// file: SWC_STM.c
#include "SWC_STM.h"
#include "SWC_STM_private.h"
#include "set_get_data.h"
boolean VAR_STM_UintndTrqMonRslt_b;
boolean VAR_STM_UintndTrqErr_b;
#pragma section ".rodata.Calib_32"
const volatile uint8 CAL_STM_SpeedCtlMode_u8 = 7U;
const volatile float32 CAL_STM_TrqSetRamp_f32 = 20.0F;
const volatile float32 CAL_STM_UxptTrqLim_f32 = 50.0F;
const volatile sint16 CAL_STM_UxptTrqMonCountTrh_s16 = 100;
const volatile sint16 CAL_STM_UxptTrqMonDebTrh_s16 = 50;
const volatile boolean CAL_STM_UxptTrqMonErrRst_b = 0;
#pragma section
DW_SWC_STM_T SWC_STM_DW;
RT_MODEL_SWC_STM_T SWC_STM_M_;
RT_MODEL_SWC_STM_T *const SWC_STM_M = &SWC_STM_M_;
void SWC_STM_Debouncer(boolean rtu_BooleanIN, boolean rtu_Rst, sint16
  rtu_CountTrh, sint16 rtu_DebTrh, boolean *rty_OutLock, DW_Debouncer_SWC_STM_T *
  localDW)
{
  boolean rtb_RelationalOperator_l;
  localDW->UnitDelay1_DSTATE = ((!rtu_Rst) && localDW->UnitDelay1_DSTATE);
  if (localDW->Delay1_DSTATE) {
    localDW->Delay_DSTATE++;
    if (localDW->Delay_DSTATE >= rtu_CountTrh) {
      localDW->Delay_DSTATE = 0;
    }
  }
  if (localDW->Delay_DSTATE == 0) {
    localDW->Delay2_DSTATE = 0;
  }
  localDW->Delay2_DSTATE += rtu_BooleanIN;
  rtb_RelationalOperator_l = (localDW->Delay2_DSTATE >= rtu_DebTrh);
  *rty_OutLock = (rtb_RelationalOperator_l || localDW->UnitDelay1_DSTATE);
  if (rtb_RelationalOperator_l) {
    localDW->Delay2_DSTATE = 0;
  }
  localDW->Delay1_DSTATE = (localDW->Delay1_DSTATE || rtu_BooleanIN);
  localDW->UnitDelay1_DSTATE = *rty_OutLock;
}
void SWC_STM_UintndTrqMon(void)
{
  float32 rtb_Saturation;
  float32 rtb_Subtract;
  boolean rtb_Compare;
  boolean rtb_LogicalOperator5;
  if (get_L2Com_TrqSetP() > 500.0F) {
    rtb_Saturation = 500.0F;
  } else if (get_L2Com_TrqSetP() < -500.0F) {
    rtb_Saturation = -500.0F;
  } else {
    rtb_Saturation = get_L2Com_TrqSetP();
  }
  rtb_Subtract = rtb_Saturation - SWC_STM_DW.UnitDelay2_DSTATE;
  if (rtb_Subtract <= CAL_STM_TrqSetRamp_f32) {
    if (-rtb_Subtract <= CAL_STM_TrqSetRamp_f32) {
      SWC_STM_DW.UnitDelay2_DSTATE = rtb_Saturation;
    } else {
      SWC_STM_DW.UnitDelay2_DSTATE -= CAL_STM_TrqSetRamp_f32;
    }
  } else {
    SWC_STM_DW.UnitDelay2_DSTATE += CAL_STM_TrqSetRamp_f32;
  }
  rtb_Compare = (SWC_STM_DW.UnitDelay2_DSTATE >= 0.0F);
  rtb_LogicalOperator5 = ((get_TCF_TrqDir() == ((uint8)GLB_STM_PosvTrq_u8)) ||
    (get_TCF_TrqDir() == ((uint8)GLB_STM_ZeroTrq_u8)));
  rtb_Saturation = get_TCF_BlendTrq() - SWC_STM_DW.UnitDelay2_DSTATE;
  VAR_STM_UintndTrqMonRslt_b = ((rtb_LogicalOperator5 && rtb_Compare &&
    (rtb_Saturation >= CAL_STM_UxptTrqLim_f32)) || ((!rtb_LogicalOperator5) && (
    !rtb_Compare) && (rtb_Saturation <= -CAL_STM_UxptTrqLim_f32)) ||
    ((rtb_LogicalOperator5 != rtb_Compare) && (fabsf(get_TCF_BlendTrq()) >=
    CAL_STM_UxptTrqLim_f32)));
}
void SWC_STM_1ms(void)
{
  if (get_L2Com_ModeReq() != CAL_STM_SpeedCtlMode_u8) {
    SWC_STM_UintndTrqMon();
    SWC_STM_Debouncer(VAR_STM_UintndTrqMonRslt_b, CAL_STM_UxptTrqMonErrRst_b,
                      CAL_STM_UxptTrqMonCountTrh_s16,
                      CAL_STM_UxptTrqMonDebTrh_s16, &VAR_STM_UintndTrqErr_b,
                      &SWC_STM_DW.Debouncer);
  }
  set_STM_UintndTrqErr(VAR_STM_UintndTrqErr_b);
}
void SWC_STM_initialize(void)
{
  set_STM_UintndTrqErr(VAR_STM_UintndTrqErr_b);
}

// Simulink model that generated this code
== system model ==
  SWC_STM_1ms : Inport
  L2Com_ModeReq : Inport
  TCF_BlendTrq : Inport
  L2Com_TrqSetP : Inport
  TCF_TrqDir : Inport
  STM_UintndTrqErr : Outport  <- 1: Subsystem#1
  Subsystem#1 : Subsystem  <- 1: L2Com_ModeReq, 2: TCF_BlendTrq, 3: L2Com_TrqSetP, 4: TCF_TrqDir, Trigger: SWC_STM_1ms
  EventListener#1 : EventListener
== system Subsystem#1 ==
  Inport#1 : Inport
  Inport#2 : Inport
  Inport#3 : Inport
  Inport#4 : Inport
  TriggerPort#1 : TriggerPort  TriggerType=function-call
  Outport#1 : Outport  <- 1: SignalConversion#1
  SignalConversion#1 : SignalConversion  <- 1: Subsystem#2
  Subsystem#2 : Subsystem  <- 1: Inport#2, 2: Inport#3, 3: Inport#4, Enable: Subsystem#3
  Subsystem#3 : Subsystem  <- 1: Inport#1
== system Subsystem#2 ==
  Inport#5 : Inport
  Inport#6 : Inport
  Inport#7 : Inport
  EnablePort#1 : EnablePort
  Outport#2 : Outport  <- 1: Debouncer
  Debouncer : Subsystem  <- 1: UintndTrqMon, 2: Constant#1, 3: Constant#2, 4: Constant#3
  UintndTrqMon : Subsystem  <- 1: Inport#5, 2: Inport#6, 3: Inport#7
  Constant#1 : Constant  Value=CAL_STM_UxptTrqMonErrRst_b
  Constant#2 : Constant  Value=CAL_STM_UxptTrqMonCountTrh_s16
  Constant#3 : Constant  Value=CAL_STM_UxptTrqMonDebTrh_s16
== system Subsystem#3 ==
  Inport#8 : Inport
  Outport#3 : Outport  <- 1: RelationalOperator#1
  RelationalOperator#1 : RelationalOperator  Operator=~=  <- 1: Inport#8, 2: Constant#4
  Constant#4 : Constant  Value=CAL_STM_SpeedCtlMode_u8
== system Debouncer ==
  BooleanIN : Inport
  Rst : Inport
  CountTrh : Inport
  DebTrh : Inport
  OutLock : Outport  <- 1: Logic#1
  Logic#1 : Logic  Operator=OR  <- 1: RelationalOperator, 2: Switch#1
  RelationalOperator : RelationalOperator  <- 1: Sum#1, 2: DebTrh
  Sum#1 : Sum  <- 1: BooleanIN, 2: Switch#2
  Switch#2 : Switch  Criteria=u2 > Threshold  <- 1: Constant#5, 2: CompareToZero#1, 3: Delay2
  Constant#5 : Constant  Value=0
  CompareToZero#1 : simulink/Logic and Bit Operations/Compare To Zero  relop===  <- 1: Subsystem#4
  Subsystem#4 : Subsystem  <- 1: CountTrh, Enable: Delay1
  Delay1 : Delay  DelayLength=1  <- 1: Logic#2
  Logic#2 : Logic  Operator=OR  <- 1: Delay1, 2: BooleanIN
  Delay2 : Delay  DelayLength=1  <- 1: Switch#3
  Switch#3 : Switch  Criteria=u2 > Threshold  <- 1: Constant#6, 2: RelationalOperator, 3: Sum#1
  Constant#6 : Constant  Value=0
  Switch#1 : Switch  Criteria=u2 ~= 0  <- 1: Constant#7, 2: Rst, 3: UnitDelay1
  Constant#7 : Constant  Value=0
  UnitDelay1 : UnitDelay  <- 1: Logic#1
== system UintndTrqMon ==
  Inport#9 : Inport
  Inport#10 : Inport
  Inport#11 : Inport
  Outport#4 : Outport  <- 1: Logic#3
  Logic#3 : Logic  Operator=OR  Inputs=3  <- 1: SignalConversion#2, 2: SignalConversion#3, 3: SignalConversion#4
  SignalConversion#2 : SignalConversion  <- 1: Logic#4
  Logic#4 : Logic  Inputs=3  <- 1: LogicalOperator5, 2: CompareToZero#2, 3: RelationalOperator#2
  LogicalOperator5 : Logic  Operator=OR  <- 1: RelationalOperator#3, 2: RelationalOperator#4
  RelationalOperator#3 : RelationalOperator  Operator===  <- 1: Inport#11, 2: Constant#8
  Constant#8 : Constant  Value=GLB_STM_PosvTrq_u8
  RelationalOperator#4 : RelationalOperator  Operator===  <- 1: Inport#11, 2: Constant#9
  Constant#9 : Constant  Value=GLB_STM_ZeroTrq_u8
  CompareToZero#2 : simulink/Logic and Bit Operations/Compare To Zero  relop=>=  <- 1: Switch#4
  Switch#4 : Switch  Criteria=u2 ~= 0  <- 1: Switch#5, 2: RelationalOperator#5, 3: Sum#2
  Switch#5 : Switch  Criteria=u2 ~= 0  <- 1: Saturation, 2: RelationalOperator#6, 3: Sum#3
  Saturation : Saturate  UpperLimit=500  LowerLimit=-500  <- 1: Inport#10
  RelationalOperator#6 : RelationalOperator  Operator=<=  <- 1: Product#1, 2: CAL_STM_TrqSetRamp_f32
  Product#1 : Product  <- 1: Constant#10, 2: Subtract
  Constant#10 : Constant  Value=-1
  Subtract : Sum  Inputs=+-  <- 1: Saturation, 2: UnitDelay2
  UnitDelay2 : UnitDelay  <- 1: Switch#4
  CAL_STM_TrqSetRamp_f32 : Constant  Value=CAL_STM_TrqSetRamp_f32
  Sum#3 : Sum  Inputs=-+  <- 1: CAL_STM_TrqSetRamp_f32, 2: UnitDelay2
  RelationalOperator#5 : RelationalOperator  Operator=<=  <- 1: Subtract, 2: CAL_STM_TrqSetRamp_f32
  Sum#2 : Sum  <- 1: CAL_STM_TrqSetRamp_f32, 2: UnitDelay2
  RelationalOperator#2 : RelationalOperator  <- 1: Sum#4, 2: Constant#11
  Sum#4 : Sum  Inputs=+-  <- 1: Inport#9, 2: Switch#4
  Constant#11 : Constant  Value=CAL_STM_UxptTrqLim_f32
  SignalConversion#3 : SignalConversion  <- 1: Logic#5
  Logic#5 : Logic  Inputs=3  <- 1: Logic#6, 2: Logic#7, 3: RelationalOperator#7
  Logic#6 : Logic  Operator=NOT  <- 1: LogicalOperator5
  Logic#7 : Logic  Operator=NOT  <- 1: CompareToZero#2
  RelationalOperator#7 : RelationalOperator  Operator=<=  <- 1: Sum#4, 2: Gain#1
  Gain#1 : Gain  Gain=-1  <- 1: Constant#12
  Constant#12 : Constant  Value=CAL_STM_UxptTrqLim_f32
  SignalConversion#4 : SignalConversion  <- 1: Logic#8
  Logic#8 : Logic  <- 1: RelationalOperator#8, 2: RelationalOperator#9
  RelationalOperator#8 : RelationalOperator  Operator=~=  <- 1: LogicalOperator5, 2: CompareToZero#2
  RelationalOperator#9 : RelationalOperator  <- 1: Abs#1, 2: Constant#13
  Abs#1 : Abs  <- 1: Inport#9
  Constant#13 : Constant  Value=CAL_STM_UxptTrqLim_f32
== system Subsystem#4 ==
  Inport#12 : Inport
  EnablePort#2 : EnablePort
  Outport#5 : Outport  <- 1: Switch#6
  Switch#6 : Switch  Criteria=u2 > Threshold  <- 1: Constant#14, 2: RelationalOperator#10, 3: Sum#5
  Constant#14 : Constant  Value=0
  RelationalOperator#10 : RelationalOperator  <- 1: Sum#5, 2: Inport#12
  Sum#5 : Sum  <- 1: Constant#15, 2: Delay
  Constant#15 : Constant
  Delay : Delay  DelayLength=1  <- 1: Switch#6
